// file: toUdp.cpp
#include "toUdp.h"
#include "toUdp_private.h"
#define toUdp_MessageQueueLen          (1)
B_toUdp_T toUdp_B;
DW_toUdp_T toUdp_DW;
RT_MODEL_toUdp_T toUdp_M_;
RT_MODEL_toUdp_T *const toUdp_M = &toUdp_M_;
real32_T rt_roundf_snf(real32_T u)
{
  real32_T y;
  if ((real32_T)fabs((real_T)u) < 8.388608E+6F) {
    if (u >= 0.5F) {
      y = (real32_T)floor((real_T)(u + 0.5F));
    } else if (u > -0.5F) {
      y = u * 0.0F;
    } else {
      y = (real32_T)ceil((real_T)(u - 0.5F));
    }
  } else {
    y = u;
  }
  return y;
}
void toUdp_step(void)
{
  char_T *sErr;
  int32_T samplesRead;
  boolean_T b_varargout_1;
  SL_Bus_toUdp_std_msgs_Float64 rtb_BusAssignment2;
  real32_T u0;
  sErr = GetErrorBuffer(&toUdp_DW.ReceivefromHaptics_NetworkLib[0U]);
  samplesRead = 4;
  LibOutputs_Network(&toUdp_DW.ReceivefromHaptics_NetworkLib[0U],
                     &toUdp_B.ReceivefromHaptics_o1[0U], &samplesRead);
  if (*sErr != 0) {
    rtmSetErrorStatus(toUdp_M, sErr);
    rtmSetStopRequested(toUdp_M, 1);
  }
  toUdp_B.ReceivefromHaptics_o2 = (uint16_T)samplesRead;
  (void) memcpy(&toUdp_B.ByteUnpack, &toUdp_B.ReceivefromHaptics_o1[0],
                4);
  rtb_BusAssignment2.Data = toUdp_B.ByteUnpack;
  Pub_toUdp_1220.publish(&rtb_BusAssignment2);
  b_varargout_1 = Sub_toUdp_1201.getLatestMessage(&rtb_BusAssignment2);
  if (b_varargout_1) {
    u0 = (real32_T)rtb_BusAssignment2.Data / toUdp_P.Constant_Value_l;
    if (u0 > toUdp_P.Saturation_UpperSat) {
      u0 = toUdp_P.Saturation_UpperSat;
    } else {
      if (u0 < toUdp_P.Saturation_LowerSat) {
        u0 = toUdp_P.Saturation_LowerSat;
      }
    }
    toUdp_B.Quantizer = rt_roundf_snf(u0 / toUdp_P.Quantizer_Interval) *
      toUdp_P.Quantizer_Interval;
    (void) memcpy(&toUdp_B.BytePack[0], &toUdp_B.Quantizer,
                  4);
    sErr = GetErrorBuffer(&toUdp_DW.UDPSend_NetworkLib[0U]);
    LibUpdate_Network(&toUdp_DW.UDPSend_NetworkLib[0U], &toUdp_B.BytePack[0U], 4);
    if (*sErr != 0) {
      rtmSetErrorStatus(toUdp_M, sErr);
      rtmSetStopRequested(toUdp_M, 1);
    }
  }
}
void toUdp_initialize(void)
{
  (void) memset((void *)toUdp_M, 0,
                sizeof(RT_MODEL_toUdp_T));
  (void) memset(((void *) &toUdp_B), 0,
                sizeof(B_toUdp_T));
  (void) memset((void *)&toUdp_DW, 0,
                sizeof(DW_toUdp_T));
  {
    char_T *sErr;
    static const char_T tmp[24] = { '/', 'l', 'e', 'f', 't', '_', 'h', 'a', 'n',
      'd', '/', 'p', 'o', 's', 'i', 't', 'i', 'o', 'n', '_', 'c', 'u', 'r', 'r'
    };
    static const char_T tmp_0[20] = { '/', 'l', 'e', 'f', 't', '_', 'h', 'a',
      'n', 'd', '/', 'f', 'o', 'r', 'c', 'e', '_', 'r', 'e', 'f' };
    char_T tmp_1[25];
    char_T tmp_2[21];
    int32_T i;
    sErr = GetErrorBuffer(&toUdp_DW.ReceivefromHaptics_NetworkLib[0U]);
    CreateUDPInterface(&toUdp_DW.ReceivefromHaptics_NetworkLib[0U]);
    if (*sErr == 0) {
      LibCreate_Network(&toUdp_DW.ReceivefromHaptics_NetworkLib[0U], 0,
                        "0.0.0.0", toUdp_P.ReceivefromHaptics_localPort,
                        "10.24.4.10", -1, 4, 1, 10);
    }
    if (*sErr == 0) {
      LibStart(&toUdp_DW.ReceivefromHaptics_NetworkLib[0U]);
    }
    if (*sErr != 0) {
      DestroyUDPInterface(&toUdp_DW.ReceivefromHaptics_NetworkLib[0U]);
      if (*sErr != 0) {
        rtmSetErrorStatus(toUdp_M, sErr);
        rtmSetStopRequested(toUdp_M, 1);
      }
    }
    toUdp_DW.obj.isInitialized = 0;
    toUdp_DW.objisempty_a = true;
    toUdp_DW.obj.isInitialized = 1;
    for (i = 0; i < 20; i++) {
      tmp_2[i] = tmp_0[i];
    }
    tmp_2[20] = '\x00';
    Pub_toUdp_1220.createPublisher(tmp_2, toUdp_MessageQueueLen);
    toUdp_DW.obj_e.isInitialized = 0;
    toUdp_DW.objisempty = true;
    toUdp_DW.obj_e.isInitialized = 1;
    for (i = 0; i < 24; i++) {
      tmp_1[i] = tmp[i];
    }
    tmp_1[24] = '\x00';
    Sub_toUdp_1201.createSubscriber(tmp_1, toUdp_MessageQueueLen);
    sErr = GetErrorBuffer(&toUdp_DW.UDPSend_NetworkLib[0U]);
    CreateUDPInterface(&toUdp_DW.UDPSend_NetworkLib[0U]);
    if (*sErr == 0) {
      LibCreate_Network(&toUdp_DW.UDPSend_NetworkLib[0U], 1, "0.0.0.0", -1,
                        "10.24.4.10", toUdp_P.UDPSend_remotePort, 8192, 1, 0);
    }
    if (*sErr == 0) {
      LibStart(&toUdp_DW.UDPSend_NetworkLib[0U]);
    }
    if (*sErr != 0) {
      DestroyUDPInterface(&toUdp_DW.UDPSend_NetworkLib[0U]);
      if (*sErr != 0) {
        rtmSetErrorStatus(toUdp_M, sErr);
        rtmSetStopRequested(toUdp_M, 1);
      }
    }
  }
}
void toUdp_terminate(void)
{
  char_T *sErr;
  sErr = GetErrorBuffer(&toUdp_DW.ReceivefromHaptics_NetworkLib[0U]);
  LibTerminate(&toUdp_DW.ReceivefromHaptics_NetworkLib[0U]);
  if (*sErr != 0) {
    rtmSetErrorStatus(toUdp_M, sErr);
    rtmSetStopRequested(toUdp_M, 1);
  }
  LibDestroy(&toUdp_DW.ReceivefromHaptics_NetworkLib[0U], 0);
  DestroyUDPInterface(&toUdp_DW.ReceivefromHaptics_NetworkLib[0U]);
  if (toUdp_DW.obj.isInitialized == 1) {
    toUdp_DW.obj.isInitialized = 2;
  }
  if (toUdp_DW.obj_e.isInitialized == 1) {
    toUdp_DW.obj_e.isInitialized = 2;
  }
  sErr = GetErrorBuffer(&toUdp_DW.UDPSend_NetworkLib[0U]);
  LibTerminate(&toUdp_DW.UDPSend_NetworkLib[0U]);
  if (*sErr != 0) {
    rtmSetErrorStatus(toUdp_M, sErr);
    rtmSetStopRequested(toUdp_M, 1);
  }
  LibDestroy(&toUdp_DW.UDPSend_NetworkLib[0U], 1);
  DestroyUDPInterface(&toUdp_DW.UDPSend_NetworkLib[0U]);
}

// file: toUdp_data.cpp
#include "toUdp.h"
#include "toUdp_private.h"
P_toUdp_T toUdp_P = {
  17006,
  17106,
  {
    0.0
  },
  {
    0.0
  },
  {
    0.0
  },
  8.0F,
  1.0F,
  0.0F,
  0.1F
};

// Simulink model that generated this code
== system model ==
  Publish#1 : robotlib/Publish  <- 1: BusAssignment2
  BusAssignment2 : BusAssignment  <- 1: BlankMessage#1, 2: DataTypeConversion#1
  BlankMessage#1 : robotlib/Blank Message
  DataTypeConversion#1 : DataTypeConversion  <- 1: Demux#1
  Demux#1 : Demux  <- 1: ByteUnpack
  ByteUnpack : etargetslib/Byte Unpack  <- 1: ReceivefromHaptics
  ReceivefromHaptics : dspnetwork/UDP Receive
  Subsystem#1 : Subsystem  <- 1: Subscribe#1/2, Enable: Subscribe#1
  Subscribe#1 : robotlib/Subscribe
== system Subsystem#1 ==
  Inport#1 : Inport
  EnablePort#1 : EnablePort
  UDPSend : dspnetwork/UDP Send  <- 1: BytePack
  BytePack : etargetslib/Byte Pack  <- 1: DataTypeConversion#2
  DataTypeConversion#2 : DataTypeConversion  <- 1: Quantizer
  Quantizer : Quantizer  QuantizationInterval=0.1  <- 1: Saturation
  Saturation : Saturate  UpperLimit=1  LowerLimit=0  <- 1: Product#1
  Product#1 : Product  Inputs=*/  <- 1: DataTypeConversion#3, 2: Constant
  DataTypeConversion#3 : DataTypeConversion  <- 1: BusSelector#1
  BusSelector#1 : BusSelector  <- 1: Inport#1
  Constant : Constant  Value=8
